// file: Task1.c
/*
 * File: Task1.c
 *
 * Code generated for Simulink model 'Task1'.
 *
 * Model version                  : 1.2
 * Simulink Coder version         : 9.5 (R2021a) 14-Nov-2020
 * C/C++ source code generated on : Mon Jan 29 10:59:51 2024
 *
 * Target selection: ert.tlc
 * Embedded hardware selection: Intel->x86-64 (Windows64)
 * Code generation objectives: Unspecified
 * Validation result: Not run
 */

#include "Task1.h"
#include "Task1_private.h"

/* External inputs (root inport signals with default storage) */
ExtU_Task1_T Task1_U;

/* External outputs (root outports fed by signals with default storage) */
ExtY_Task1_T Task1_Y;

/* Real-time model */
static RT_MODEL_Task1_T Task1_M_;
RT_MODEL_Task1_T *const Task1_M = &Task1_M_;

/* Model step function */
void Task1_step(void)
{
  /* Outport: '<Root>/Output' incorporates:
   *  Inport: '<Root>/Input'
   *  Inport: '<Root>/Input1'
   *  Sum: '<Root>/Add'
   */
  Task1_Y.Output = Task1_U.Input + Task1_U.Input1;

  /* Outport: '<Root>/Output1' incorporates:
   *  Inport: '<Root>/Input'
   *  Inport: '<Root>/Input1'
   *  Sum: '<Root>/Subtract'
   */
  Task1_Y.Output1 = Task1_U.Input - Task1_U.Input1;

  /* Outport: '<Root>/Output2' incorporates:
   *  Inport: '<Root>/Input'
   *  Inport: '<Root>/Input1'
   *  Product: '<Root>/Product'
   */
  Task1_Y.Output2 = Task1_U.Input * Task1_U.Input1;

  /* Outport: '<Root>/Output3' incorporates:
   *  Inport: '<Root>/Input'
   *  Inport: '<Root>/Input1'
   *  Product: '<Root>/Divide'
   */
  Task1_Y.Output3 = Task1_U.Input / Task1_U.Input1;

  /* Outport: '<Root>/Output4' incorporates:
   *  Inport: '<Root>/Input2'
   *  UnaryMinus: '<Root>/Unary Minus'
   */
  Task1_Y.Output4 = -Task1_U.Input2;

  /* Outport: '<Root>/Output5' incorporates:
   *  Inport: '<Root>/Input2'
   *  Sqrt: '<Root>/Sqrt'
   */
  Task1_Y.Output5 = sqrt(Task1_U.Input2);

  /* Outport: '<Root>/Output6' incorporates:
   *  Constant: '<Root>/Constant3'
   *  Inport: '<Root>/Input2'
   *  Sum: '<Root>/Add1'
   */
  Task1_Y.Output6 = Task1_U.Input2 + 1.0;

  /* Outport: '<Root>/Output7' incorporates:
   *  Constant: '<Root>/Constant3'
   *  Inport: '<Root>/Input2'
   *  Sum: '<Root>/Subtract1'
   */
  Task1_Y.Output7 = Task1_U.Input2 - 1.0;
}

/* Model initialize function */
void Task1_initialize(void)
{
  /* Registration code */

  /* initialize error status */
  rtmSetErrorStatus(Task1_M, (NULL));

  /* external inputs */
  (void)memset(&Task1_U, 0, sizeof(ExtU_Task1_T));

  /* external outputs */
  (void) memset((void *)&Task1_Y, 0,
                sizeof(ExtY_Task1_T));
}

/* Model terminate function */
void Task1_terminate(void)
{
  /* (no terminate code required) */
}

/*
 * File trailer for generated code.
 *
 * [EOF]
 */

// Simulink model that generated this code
simulink model "Task1"  (R2021a)
settings: Solver=FixedStepDiscrete  StartTime=0.0  StopTime=10.0  RelTol=1e-3  EnableMultiTasking=on

== system Task1 ==
  Input : Inport
  Input1 : Inport  Port=2
  Input2 : Inport  Port=3
  Add : Sum
  Add1 : Sum
  Constant3 : Constant
  Divide : Product  Inputs=*/
  Product : Product
  Sqrt : Sqrt  SaturateOnIntegerOverflow=on
  Subtract : Sum  Inputs=+-
  Subtract1 : Sum  Inputs=+-
  Unary Minus : UnaryMinus  SaturateOnIntegerOverflow=on
  Output : Outport
  Output1 : Outport  Port=2
  Output2 : Outport  Port=3
  Output3 : Outport  Port=4
  Output4 : Outport  Port=5
  Output5 : Outport  Port=6
  Output6 : Outport  Port=7
  Output7 : Outport  Port=8
  wires:
  Constant3/1 -> Add1/2, Subtract1/2
  Product/1 -> Output2/1
  Divide/1 -> Output3/1
  Subtract/1 -> Output1/1
  Add/1 -> Output/1
  Input/1 -> Add/1, Divide/1, Product/1, Subtract/1
  Input1/1 -> Add/2, Subtract/2, Divide/2, Product/2
  Input2/1 -> Subtract1/1, Add1/1, Unary Minus/1, Sqrt/1
  Subtract1/1 -> Output7/1
  Add1/1 -> Output6/1
  Sqrt/1 -> Output5/1
  Unary Minus/1 -> Output4/1
